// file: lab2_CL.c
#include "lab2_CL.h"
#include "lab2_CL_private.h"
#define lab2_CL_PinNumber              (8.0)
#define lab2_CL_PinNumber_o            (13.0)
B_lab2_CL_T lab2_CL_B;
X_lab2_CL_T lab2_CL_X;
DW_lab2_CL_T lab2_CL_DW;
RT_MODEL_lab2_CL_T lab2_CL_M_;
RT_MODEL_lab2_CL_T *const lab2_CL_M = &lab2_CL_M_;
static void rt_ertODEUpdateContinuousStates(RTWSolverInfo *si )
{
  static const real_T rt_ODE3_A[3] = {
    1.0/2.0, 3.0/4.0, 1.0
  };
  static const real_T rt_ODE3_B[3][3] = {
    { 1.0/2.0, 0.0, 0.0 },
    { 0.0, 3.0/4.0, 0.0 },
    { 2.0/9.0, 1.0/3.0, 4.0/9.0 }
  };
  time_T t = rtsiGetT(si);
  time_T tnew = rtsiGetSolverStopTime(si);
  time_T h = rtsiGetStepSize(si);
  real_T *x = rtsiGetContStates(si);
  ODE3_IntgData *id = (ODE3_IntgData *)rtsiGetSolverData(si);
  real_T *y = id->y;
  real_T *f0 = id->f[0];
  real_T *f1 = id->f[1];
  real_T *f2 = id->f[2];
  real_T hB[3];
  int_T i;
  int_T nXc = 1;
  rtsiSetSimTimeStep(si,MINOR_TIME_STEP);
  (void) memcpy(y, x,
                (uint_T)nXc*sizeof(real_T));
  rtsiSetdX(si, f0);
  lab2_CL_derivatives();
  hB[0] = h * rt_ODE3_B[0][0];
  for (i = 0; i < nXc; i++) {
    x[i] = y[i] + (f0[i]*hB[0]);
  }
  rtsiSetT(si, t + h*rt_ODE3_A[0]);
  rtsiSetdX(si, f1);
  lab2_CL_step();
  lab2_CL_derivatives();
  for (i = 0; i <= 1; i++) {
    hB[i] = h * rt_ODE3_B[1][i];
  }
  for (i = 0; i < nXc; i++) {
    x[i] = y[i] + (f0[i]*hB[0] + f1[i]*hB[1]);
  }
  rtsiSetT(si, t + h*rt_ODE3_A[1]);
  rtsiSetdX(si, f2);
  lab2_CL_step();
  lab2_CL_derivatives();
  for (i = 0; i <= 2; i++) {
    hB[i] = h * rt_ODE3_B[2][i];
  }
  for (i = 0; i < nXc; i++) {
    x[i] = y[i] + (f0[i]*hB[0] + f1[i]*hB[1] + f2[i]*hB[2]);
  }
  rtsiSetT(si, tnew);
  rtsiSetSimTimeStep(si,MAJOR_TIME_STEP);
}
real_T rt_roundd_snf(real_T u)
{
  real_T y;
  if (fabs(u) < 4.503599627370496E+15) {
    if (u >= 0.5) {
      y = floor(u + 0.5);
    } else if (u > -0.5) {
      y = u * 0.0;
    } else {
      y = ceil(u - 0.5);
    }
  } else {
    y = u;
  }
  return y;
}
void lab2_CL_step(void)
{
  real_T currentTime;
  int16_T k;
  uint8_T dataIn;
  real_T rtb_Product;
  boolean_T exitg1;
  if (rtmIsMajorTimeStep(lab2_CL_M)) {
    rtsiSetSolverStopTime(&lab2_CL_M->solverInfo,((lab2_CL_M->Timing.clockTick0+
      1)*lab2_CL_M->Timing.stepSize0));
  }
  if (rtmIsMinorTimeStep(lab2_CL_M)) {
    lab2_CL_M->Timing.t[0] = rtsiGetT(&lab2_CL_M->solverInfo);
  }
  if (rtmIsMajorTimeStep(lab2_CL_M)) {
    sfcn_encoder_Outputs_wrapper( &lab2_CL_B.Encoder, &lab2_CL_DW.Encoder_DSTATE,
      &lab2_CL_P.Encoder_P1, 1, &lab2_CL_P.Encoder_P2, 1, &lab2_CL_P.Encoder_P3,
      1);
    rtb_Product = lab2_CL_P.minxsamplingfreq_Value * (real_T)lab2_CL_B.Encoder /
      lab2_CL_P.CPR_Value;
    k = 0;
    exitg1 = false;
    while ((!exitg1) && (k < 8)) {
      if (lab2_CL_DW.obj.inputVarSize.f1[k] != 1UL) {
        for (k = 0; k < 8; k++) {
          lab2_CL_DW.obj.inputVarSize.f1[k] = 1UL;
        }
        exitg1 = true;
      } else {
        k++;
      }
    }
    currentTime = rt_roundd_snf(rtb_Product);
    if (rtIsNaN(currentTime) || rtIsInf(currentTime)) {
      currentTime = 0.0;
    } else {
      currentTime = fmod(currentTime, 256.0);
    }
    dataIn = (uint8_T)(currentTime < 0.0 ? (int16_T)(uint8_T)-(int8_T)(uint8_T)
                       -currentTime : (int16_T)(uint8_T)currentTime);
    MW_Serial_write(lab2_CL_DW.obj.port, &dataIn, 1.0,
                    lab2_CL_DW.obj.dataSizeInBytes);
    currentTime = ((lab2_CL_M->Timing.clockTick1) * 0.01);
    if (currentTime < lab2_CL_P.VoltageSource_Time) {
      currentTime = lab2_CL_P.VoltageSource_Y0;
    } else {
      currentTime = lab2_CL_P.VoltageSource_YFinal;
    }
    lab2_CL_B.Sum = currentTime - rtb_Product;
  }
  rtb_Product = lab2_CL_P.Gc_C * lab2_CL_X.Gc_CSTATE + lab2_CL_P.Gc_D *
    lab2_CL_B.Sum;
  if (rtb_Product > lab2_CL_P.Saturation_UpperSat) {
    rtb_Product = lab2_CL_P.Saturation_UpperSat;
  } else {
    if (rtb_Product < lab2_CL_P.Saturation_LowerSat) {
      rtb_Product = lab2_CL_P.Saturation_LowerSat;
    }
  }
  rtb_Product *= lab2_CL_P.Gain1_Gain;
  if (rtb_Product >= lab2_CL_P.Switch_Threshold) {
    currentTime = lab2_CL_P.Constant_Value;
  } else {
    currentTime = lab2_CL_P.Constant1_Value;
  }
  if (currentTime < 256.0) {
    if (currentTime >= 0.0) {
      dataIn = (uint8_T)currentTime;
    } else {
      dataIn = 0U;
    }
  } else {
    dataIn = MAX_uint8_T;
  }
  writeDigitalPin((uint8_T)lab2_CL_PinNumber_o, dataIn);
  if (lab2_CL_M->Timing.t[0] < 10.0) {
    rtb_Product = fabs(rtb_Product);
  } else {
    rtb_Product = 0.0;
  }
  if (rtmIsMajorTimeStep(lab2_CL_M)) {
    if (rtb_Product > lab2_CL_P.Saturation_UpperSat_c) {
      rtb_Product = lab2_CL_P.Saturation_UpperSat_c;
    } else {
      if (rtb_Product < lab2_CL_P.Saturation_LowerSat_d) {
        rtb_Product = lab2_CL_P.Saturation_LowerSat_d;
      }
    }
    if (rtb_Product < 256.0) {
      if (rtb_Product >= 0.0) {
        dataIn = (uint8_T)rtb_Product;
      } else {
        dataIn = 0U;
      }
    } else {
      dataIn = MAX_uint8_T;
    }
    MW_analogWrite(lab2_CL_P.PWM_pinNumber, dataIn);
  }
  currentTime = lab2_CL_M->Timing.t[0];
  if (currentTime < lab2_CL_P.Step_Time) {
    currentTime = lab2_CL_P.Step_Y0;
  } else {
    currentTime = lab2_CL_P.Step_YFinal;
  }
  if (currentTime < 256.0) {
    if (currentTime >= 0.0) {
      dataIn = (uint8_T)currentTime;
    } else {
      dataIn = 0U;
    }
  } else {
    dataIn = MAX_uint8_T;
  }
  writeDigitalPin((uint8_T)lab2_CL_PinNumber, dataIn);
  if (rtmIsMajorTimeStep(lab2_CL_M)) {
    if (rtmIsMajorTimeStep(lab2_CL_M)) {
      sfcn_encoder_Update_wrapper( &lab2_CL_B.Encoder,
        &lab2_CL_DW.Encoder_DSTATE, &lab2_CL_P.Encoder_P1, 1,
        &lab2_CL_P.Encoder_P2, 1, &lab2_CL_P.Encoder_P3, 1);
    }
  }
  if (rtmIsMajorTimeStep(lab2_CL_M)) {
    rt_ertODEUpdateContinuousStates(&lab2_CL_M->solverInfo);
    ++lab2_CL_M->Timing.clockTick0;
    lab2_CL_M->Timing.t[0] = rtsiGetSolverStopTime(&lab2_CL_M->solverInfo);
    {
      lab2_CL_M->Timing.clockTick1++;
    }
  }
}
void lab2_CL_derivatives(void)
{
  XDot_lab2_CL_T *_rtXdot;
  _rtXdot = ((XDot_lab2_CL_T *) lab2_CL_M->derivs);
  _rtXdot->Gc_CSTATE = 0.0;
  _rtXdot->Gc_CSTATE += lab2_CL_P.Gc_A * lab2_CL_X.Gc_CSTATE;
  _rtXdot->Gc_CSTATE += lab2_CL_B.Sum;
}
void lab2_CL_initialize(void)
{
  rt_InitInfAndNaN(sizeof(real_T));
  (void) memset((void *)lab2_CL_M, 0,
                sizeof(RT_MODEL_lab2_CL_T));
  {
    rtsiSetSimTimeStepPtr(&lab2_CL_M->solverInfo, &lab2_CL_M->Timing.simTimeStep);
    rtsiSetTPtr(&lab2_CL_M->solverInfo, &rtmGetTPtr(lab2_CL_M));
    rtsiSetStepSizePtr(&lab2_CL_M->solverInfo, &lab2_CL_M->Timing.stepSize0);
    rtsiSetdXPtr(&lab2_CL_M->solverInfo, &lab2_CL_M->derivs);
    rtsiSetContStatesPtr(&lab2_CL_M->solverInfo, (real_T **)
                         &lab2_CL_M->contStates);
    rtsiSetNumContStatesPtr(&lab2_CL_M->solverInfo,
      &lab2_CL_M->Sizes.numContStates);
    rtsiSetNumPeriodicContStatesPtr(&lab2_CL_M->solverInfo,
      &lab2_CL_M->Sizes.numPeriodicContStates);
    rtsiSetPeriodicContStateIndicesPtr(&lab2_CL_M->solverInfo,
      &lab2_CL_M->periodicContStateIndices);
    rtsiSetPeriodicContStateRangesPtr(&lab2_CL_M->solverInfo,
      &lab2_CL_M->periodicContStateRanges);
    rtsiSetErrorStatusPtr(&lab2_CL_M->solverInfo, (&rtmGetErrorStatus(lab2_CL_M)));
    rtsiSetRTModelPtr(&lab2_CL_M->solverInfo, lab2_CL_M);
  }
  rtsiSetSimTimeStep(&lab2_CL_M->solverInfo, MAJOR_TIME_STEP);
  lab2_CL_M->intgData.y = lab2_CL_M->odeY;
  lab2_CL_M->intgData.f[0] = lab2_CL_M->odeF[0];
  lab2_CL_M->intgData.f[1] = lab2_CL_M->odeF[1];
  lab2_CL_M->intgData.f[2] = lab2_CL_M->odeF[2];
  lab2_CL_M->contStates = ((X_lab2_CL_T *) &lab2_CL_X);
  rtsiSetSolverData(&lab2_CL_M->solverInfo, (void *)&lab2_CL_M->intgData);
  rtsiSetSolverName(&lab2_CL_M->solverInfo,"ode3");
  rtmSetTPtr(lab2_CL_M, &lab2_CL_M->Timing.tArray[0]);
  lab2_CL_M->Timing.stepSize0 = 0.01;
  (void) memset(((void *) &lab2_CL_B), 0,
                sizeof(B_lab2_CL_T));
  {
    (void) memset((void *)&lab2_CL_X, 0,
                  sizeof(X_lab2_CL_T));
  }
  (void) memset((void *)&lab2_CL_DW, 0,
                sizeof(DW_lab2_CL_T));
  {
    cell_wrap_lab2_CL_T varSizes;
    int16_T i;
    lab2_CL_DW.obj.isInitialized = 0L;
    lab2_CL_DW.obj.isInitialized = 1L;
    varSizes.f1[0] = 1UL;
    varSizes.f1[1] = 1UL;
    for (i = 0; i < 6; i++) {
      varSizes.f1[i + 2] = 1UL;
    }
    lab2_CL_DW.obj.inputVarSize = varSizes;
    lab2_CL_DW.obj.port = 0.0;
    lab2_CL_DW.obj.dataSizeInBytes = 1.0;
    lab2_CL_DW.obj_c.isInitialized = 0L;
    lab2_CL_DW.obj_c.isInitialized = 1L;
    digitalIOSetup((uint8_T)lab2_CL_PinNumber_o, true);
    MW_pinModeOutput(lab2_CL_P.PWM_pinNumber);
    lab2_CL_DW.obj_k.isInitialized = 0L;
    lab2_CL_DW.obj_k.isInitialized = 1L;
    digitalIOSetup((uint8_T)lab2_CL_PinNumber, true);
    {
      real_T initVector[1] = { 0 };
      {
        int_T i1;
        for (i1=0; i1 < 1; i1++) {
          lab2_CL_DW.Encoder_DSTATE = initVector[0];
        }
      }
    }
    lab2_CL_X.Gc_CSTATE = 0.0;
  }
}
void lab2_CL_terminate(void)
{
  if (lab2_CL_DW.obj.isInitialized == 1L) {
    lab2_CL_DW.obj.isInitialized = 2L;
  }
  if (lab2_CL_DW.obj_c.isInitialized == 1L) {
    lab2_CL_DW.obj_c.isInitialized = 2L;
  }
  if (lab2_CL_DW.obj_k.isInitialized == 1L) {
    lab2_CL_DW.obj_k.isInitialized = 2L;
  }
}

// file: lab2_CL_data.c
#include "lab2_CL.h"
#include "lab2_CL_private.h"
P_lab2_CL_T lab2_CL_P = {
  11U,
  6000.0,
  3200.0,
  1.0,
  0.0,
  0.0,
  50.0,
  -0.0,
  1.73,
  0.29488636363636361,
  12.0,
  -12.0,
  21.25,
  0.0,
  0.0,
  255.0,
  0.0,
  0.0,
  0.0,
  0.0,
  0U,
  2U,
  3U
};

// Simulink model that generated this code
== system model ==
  SerialTransmit#1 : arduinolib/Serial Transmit  <- 1: DataTypeConversion#1
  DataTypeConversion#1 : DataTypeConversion  <- 1: Product
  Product : Product  Inputs=**/  <- 1: minxsamplingfreq, 2: DataTypeConversion#2, 3: CPR
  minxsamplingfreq : Constant  Value=6000
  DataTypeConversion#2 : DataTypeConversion  <- 1: Encoder
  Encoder : S-Function  FunctionName=sfcn_encoder
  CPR : Constant  Value=3200
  DigitalOutput#1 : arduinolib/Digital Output  pinNumber=13  <- 1: hardlim#1
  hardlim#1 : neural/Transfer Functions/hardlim  <- 1: Gain1
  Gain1 : Gain  Gain=255/12  <- 1: Saturation
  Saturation : Saturate  UpperLimit=12  LowerLimit=-12  <- 1: Gc
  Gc : TransferFcn  Numerator=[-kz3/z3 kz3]  Denominator=[1 0]  <- 1: Sum
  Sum : Sum  Inputs=+-  <- 1: VoltageSource, 2: Product
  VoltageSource : Step  Time=0  After=50
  PWM : arduinolib/PWM  pinNumber=11  <- 1: Saturate#1
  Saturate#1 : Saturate  UpperLimit=255  LowerLimit=0  <- 1: MATLABFunction#1
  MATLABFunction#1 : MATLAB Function  <- 1: Abs#1, 2: Clock#1
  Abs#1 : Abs  <- 1: Gain1
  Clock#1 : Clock
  DigitalOutput#2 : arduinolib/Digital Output  pinNumber=8  <- 1: Step
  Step : Step  Time=0  After=0
== matlab function MATLABFunction#1 ==
function y = fcn(u,c)
%#codegen
if c<10
    y = u;
else
    y=0;
end
